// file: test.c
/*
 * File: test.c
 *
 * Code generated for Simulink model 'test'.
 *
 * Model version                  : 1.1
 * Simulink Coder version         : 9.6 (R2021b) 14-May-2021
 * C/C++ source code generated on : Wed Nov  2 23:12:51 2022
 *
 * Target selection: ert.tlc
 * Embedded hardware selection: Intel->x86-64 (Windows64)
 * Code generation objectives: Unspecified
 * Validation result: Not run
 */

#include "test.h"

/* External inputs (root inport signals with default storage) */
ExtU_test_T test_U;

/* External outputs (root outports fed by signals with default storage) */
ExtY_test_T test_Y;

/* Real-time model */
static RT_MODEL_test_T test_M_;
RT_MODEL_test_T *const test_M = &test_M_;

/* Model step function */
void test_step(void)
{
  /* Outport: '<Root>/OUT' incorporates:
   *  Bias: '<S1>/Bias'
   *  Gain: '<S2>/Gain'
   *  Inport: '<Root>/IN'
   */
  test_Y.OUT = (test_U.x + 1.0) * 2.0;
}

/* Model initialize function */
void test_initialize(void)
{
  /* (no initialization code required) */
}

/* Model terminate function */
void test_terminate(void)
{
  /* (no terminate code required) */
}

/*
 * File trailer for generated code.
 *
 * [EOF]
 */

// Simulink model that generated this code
simulink model "test"  (R2021b)
settings: Solver=VariableStepAuto  StartTime=0.0  StopTime=10.0  RelTol=1e-3

== system test ==
  IN : Inport
  A : Subsystem
  B : Subsystem
  OUT : Outport
  wires:
  IN/1 -> A/1(Inport)  "x"
  A/1(Out1) -> B/1(In1)  "y"
  B/1(Outport) -> OUT/1  "z"

== system test/A ==
  Inport : Inport
  Bias : Bias  Bias=1
  Out1 : Outport
  wires:
  Inport/1 -> Bias/1
  Bias/1 -> Out1/1

== system test/B ==
  In1 : Inport
  Gain : Gain  Gain=2
  Outport : Outport
  wires:
  In1/1 -> Gain/1
  Gain/1 -> Outport/1
